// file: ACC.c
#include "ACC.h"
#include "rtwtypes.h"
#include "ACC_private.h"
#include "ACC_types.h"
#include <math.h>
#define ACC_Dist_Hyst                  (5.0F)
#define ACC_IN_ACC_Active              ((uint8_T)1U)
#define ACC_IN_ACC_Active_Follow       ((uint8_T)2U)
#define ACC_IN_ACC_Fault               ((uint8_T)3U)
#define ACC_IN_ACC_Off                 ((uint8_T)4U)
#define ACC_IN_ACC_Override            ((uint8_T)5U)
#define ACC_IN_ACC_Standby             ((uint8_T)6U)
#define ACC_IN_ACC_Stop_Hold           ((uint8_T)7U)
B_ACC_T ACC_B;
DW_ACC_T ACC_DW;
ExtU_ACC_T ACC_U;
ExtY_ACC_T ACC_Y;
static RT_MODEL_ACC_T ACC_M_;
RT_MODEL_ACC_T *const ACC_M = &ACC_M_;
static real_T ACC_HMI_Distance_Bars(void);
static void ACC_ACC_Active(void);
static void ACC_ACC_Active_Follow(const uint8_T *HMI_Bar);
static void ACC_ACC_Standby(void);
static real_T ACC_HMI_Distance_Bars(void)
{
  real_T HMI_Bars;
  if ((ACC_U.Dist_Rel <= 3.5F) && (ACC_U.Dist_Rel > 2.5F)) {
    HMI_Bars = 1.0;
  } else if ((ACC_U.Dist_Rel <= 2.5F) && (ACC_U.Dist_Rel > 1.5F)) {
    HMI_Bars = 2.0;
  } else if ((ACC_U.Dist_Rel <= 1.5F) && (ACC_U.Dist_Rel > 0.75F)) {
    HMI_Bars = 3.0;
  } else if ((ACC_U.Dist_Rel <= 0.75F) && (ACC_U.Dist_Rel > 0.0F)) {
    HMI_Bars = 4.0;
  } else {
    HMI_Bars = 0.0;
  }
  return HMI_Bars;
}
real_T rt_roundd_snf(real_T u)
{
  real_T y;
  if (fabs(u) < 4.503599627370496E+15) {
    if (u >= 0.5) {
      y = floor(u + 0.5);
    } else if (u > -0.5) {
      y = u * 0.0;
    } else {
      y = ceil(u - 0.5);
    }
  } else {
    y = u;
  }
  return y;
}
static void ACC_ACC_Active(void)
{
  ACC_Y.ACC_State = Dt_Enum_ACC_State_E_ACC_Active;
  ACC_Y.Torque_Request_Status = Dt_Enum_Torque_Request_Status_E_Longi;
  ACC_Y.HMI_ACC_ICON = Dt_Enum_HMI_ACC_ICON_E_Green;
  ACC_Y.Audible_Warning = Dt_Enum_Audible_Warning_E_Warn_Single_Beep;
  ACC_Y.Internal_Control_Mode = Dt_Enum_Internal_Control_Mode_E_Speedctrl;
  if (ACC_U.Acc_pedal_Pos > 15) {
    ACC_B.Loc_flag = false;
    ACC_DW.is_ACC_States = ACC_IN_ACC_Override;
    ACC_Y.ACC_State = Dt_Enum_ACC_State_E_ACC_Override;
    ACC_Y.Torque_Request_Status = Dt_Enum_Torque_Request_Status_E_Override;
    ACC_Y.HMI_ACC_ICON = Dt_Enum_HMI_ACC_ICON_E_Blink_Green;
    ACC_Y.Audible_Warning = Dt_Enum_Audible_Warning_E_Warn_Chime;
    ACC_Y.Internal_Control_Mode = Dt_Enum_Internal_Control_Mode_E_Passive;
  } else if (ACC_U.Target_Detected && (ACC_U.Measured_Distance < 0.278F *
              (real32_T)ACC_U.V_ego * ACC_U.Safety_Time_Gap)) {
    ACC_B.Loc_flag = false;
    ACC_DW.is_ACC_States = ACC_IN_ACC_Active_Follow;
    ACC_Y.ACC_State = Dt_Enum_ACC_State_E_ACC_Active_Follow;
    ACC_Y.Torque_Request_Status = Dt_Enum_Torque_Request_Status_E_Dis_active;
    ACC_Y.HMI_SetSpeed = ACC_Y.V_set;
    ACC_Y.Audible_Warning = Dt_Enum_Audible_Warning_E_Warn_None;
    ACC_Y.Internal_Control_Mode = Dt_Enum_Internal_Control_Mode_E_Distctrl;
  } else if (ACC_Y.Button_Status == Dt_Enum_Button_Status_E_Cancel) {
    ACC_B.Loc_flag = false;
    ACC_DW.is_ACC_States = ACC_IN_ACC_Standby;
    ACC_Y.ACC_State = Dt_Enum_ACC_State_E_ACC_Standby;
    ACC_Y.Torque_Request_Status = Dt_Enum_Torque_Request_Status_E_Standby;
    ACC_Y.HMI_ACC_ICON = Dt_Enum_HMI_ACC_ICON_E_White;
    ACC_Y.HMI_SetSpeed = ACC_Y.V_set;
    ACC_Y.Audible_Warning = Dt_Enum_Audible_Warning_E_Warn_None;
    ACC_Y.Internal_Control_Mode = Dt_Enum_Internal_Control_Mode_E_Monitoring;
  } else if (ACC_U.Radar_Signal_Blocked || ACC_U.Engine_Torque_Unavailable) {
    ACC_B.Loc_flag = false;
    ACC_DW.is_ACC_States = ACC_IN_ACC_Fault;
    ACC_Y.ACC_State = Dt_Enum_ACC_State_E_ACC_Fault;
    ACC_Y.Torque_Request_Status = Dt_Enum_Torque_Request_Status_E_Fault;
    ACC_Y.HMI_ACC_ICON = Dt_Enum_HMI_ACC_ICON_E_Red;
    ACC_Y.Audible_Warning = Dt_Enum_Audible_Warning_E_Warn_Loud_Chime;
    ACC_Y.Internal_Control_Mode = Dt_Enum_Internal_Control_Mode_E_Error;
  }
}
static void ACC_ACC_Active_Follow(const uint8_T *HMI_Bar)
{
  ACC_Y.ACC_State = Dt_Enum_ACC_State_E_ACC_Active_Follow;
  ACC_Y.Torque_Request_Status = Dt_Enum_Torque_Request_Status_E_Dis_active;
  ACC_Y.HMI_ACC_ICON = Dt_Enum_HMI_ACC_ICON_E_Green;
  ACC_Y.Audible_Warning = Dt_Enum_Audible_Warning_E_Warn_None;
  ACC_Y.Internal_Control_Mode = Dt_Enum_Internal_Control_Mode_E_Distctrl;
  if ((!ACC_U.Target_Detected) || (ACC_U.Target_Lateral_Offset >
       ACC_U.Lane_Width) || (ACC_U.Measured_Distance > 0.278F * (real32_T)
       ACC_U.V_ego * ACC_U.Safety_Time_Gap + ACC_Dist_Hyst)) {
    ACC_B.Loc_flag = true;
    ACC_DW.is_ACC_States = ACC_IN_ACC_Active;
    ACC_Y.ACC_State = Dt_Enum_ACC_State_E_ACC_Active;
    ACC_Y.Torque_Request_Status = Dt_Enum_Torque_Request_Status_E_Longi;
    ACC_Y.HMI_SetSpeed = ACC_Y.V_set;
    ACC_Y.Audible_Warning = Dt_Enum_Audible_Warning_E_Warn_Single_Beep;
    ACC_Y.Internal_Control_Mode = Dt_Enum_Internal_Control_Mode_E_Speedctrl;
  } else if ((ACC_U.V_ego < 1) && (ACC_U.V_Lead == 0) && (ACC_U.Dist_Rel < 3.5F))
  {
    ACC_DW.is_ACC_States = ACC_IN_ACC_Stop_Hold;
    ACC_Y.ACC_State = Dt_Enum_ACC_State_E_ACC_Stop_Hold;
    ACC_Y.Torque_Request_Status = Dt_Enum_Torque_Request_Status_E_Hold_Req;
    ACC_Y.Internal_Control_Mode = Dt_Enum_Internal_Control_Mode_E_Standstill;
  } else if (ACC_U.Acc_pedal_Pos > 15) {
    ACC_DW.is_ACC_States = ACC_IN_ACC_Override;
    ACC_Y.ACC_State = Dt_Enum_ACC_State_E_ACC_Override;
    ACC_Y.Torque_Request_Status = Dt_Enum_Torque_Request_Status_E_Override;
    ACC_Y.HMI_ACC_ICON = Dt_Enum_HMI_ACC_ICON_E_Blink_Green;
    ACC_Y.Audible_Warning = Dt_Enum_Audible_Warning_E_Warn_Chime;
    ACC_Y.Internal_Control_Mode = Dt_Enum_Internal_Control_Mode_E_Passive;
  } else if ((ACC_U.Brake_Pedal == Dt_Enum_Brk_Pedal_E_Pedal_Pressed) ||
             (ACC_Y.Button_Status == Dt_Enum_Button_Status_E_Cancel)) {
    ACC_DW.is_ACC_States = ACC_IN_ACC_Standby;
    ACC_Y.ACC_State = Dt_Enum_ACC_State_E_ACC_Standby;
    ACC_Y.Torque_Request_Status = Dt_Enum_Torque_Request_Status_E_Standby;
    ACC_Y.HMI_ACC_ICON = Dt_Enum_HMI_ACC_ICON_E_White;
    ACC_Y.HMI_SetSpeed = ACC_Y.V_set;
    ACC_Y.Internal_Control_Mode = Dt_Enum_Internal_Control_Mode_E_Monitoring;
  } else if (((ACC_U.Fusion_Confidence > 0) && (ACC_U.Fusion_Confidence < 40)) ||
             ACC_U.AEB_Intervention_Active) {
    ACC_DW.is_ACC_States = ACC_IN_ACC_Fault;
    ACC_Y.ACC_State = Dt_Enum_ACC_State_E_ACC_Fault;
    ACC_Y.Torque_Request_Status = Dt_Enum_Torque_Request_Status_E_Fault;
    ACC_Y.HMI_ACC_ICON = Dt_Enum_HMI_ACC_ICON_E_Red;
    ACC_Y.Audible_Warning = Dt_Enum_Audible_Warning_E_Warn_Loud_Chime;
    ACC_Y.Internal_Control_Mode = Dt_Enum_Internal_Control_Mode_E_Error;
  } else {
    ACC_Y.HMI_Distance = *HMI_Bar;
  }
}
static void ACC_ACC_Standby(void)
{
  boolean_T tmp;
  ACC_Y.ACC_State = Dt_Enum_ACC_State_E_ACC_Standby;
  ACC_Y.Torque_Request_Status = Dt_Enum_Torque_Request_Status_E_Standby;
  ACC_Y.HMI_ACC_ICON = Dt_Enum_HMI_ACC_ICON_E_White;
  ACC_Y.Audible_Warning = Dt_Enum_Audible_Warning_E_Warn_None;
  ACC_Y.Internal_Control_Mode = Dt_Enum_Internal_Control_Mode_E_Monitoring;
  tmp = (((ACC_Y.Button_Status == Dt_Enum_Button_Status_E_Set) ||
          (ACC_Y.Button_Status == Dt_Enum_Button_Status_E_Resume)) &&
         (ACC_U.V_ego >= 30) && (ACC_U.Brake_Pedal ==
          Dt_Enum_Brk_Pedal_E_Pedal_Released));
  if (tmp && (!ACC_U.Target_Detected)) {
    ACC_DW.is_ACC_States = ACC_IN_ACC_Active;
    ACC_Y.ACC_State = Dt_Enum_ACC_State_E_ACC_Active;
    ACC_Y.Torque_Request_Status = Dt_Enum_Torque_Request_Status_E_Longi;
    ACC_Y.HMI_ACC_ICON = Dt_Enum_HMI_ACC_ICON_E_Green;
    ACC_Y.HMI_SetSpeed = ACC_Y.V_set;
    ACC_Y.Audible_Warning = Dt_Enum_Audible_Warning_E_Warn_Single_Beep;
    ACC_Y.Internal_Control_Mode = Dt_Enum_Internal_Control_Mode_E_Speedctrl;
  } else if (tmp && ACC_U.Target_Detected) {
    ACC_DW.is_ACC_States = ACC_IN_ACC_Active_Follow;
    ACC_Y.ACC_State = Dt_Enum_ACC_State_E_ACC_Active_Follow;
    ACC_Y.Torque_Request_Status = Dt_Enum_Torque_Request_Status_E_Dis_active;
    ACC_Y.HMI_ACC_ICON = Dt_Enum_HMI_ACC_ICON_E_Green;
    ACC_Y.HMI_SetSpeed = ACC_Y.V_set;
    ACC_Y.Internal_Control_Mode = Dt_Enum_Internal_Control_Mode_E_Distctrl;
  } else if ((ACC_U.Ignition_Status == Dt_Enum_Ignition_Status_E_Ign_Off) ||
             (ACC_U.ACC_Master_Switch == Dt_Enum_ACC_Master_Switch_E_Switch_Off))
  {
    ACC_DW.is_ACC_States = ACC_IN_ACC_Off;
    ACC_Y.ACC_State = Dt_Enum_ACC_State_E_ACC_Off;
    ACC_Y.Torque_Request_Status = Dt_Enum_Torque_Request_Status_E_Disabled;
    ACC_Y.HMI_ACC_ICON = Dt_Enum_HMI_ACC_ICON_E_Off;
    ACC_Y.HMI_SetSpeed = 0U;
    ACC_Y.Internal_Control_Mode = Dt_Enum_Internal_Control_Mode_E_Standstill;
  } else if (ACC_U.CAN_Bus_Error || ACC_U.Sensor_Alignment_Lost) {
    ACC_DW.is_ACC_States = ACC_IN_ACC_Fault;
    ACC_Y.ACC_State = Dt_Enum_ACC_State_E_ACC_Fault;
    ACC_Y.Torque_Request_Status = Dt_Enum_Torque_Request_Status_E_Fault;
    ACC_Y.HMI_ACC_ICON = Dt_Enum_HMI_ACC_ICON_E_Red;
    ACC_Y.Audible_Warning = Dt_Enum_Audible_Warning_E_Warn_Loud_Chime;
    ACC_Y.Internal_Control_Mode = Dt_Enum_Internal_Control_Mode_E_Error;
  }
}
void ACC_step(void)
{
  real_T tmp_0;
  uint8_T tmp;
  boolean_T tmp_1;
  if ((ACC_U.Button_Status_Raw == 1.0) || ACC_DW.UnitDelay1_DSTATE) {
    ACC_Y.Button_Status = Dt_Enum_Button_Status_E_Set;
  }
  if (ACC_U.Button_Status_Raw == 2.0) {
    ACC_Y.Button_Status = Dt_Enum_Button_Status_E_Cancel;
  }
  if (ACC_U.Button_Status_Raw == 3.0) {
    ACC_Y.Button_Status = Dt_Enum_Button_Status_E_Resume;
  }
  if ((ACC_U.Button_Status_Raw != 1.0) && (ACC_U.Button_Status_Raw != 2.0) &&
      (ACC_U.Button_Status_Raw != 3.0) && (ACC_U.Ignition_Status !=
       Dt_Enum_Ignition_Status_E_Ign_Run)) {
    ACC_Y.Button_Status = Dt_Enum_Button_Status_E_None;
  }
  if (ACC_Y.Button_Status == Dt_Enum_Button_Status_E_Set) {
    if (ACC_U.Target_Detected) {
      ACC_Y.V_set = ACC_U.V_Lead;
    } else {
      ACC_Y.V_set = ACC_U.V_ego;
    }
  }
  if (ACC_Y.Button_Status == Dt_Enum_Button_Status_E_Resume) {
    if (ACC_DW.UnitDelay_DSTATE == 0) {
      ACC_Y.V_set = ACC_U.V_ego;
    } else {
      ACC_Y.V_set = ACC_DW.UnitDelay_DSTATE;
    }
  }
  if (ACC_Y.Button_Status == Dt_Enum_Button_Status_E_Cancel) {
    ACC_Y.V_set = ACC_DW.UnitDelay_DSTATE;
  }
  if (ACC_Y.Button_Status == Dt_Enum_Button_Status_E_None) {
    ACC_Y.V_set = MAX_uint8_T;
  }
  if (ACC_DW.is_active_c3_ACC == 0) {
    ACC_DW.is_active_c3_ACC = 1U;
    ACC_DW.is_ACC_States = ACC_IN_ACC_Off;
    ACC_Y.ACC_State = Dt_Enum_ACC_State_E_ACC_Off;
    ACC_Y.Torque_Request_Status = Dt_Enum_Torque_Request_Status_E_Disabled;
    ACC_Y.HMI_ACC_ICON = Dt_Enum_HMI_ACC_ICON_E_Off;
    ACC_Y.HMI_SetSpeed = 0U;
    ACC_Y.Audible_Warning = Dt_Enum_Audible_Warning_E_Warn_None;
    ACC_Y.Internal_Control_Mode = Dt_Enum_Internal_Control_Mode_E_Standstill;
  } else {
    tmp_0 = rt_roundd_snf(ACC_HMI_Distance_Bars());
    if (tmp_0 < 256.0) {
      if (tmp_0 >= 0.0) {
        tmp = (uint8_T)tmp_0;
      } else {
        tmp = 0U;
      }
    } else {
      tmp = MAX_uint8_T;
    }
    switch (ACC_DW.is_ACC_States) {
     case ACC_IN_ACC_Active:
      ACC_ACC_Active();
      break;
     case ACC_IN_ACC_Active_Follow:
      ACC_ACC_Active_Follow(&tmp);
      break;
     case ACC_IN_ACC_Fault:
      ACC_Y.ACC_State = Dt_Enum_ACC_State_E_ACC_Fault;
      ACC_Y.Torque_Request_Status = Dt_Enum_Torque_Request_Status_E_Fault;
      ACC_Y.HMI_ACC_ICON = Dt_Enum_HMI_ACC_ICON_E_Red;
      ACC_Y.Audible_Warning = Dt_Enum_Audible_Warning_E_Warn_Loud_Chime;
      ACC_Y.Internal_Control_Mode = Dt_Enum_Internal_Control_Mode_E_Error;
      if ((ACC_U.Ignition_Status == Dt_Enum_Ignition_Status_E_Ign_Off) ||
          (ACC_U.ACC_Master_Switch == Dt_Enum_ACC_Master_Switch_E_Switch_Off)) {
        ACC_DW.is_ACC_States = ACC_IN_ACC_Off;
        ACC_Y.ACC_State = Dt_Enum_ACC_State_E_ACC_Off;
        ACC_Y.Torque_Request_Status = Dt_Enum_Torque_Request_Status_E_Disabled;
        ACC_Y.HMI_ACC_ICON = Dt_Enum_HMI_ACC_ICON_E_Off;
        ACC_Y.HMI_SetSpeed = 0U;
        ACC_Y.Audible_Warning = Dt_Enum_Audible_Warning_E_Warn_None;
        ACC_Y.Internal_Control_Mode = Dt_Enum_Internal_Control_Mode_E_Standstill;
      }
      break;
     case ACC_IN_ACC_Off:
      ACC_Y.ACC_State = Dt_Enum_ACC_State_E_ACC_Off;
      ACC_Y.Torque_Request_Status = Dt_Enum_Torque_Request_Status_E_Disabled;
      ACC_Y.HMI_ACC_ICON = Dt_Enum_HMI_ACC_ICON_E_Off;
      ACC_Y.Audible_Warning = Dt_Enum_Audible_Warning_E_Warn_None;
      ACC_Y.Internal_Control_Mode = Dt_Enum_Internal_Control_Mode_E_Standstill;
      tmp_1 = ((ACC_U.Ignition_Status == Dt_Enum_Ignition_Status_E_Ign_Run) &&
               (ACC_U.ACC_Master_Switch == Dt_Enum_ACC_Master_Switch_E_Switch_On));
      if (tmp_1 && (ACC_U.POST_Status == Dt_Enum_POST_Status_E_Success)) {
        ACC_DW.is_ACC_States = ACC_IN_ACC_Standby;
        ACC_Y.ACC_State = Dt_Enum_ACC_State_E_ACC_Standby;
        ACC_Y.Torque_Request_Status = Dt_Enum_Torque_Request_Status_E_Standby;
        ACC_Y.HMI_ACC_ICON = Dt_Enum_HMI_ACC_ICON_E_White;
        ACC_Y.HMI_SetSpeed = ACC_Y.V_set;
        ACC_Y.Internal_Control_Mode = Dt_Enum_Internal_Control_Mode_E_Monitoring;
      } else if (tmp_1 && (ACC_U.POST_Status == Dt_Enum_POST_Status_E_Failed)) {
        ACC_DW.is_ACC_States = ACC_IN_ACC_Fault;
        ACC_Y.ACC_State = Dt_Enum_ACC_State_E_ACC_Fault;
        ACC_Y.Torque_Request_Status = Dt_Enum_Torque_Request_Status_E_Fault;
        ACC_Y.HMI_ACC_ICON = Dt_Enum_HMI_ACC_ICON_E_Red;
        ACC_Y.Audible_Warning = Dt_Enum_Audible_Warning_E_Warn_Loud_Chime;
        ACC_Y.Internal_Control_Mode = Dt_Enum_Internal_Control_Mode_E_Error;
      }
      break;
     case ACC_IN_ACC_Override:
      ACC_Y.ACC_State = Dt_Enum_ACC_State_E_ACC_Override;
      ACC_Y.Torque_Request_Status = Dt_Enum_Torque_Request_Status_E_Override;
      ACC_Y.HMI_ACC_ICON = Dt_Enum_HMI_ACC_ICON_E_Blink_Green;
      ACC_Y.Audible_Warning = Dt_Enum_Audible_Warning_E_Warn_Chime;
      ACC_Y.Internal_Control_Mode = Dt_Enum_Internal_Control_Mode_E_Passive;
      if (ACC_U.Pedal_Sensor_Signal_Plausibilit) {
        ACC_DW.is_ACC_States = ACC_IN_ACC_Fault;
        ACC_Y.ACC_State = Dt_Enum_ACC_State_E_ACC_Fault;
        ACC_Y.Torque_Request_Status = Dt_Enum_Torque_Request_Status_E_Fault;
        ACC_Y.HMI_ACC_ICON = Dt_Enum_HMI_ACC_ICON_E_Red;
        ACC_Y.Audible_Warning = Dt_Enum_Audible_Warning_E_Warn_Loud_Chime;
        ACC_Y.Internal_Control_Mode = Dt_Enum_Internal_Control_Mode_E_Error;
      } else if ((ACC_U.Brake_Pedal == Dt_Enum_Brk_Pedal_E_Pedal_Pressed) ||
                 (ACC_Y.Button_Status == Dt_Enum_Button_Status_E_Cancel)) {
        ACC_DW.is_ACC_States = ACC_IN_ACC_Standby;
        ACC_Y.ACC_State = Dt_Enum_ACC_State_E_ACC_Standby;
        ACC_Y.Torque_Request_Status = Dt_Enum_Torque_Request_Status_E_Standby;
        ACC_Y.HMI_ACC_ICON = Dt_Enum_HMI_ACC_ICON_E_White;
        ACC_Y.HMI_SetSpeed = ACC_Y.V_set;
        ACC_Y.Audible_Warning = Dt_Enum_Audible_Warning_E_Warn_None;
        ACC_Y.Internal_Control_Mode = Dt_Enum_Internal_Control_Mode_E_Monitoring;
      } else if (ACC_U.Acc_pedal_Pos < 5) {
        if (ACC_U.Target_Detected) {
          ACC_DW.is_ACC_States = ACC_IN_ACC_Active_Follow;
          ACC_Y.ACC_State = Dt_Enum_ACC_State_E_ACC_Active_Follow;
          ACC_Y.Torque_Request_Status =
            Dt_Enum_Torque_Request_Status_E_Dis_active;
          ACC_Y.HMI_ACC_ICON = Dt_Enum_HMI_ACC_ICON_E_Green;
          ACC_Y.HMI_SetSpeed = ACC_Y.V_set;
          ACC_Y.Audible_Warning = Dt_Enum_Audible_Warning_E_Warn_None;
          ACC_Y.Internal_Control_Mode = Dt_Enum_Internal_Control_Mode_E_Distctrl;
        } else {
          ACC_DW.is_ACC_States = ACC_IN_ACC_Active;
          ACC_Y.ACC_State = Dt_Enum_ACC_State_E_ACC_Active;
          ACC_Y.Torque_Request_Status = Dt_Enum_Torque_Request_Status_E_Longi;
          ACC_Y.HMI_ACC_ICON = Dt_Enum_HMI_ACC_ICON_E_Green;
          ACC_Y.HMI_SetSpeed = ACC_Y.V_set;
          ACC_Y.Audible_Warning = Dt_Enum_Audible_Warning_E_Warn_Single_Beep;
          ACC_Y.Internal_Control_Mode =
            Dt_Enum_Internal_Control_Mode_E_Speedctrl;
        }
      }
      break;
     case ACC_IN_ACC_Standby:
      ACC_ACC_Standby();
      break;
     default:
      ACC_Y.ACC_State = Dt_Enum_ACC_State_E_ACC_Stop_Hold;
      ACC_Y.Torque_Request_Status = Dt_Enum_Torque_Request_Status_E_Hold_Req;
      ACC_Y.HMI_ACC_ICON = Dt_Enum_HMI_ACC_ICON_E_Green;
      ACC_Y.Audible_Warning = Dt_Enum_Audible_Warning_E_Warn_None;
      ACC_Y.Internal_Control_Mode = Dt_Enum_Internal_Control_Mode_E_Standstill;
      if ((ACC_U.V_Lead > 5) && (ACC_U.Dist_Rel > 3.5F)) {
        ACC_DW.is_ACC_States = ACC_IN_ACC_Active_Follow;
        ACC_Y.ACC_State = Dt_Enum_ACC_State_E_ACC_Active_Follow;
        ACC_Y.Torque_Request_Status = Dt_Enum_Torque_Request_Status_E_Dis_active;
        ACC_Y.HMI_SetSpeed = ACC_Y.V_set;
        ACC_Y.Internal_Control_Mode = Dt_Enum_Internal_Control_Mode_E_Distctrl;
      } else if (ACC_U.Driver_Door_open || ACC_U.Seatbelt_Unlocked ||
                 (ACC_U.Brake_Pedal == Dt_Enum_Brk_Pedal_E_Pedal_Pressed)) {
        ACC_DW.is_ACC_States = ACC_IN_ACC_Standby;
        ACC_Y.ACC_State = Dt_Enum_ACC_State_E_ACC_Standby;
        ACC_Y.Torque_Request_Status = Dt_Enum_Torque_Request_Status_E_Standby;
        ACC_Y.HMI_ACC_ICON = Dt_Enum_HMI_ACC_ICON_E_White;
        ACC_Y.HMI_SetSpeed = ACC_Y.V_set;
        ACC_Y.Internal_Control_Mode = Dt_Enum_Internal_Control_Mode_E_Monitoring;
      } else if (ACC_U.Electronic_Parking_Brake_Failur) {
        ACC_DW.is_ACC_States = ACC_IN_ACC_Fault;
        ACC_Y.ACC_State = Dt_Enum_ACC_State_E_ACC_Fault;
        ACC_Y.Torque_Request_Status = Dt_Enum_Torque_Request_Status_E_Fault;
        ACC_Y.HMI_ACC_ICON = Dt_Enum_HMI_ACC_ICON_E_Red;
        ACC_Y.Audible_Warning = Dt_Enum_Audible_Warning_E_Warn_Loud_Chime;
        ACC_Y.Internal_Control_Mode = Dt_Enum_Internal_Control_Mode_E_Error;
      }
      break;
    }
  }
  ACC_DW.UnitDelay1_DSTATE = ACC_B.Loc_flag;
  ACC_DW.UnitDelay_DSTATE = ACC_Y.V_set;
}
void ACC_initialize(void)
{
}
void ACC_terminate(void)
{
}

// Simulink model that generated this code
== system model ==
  Button_Status_Raw : Inport
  ACC_Master_Switch : Inport
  AEB_Intervention_Active : Inport
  Acc_pedal_Pos : Inport
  Brake_Pedal : Inport
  CAN_Bus_Error : Inport
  Dist_Rel : Inport
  Driver_Door_open : Inport
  Inport#1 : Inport
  Engine_Torque_Unavailable : Inport
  Fusion_Confidence : Inport
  Ignition_Status : Inport
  Lane_Width : Inport
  Measured_Distance : Inport
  POST_Status : Inport
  Inport#2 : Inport
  Radar_Signal_Blocked : Inport
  Target_Detected : Inport
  Seatbelt_Unlocked : Inport
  Sensor_Alignment_Lost : Inport
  Target_Lateral_Offset : Inport
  V_Lead : Inport
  V_ego : Inport
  Safety_Time_Gap : Inport
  Audible_Warning : Outport  <- 1: ACC
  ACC : Stateflow chart  <- 1: ACC_Master_Switch, 2: AEB_Intervention_Active, 3: Acc_pedal_Pos, 4: Brake_Pedal, 5: CAN_Bus_Error, 6: Dist_Rel, 7: Driver_Door_open, 8: Inport#1, 9: Engine_Torque_Unavailable, 10: Fusion_Confidence, 11: Ignition_Status, 12: Lane_Width, 13: Measured_Distance, 14: POST_Status, 15: Inport#2, 16: Radar_Signal_Blocked, 17: Target_Detected, 18: Seatbelt_Unlocked, 19: Sensor_Alignment_Lost, 20: Target_Lateral_Offset, 21: V_Lead, 22: V_ego, 23: Stateflowchart#1, 24: Safety_Time_Gap, 25: Stateflowchart#2
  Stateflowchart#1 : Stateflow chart  <- 1: Button_Status_Raw, 2: Ignition_Status, 3: UnitDelay1
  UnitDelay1 : UnitDelay  <- 1: ACC/8
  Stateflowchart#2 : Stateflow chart  <- 1: Stateflowchart#1, 2: V_ego, 3: UnitDelay, 4: V_Lead, 5: Target_Detected
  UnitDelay : UnitDelay  <- 1: Stateflowchart#2
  HMI_ACC_ICON : Outport  <- 1: ACC/2
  HMI_SetSpeed : Outport  <- 1: ACC/3
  Torque_Request_Status : Outport  <- 1: ACC/4
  Internal_Control_Mode : Outport  <- 1: ACC/5
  HMI_Distance : Outport  <- 1: ACC/6
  ACC_State : Outport  <- 1: ACC/7
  Button_Status : Outport  <- 1: Stateflowchart#1
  V_set : Outport  <- 1: Stateflowchart#2
== stateflow chart Stateflowchart#1 ==
  (default) -> (junction 29)
  (junction 29) -> (junction 4) [order 1] : [Button_Status_Raw == 1 || Loc_flag]
  (junction 29) -> (junction 8) [order 2]
  (junction 4) -> (junction 6) : {Button_Status = Set}
  (junction 6) -> (junction 8)
  (junction 8) -> (junction 11)
  (junction 11) -> (junction 13) [order 1] : [Button_Status_Raw == 2]
  (junction 11) -> (junction 17) [order 2]
  (junction 13) -> (junction 15) : {Button_Status = Cancel}
  (junction 15) -> (junction 17)
  (junction 17) -> (junction 20)
  (junction 20) -> (junction 32) [order 1] : [Button_Status_Raw == 3]
  (junction 20) -> (junction 35) [order 2]
  (junction 32) -> (junction 34) : {Button_Status = Resume}
  (junction 34) -> (junction 35)
  (junction 35) -> (junction 40)
  (junction 40) -> (junction 39) [order 1] : [(Button_Status_Raw ~= 1 && Button_Status_Raw ~=2 && Button_Status_Raw ~= 3) && (Ignition_Status ~= Ign_Run)]
  (junction 40) -> (junction 42) [order 2]
  (junction 39) -> (junction 41) : {Button_Status = None}
  (junction 41) -> (junction 42)
  data: Button_Status_Raw input; Button_Status output Enum: Dt_Enum_Button_Status_E; Ignition_Status input Enum: Dt_Enum_Ignition_Status_E; Loc_flag input

== stateflow chart Stateflowchart#2 ==
  (default) -> (junction 2)
  (junction 2) -> (junction 3) [order 1] : [ Button_Status ==Set]
  (junction 3) -> (junction 42) [order 1] : [Target_Detected]
  (junction 2) -> (junction 4) [order 2]
  (junction 3) -> (junction 1) [order 2] : {V_set = V_ego}
  (junction 42) -> (junction 44) : {V_set = V_Lead}
  (junction 1) -> (junction 4)
  (junction 44) -> (junction 1)
  (junction 4) -> (junction 9)
  (junction 9) -> (junction 7) [order 1] : [Button_Status == Resume]
  (junction 7) -> (junction 34) [order 2]
  (junction 34) -> (junction 10) : {V_set = V_set_Prev}
  (junction 9) -> (junction 5) [order 2]
  (junction 7) -> (junction 39) [order 1] : [V_set_Prev ==0 ]
  (junction 39) -> (junction 10) : {V_set = V_ego}
  (junction 10) -> (junction 5)
  (junction 5) -> (junction 53)
  (junction 53) -> (junction 55) [order 1] : [Button_Status == Cancel]
  (junction 53) -> (junction 59) [order 2]
  (junction 55) -> (junction 57) : {V_set = V_set_Prev}
  (junction 57) -> (junction 59)
  (junction 59) -> (junction 62)
  (junction 62) -> (junction 64) [order 1] : [Button_Status == None]
  (junction 62) -> (junction 68) [order 2]
  (junction 64) -> (junction 66) : {V_set = 255}
  (junction 66) -> (junction 68)
  data: Button_Status input Enum: Dt_Enum_Button_Status_E; V_ego input uint8; V_set output uint8; V_set_Prev input uint8; V_Lead input; Target_Detected input

== stateflow chart ACC ==
  state HMI_Bars = HMI_Distance_Bars [function]
    (junction 523) -> (junction 533) : {HMI_Bars=1}
    (junction 521) -> (junction 523) [order 1] : [Dist_Rel <= 3.5 && Dist_Rel > 2.5]
    (junction 524) -> (junction 533) : {HMI_Bars=2}
    (junction 521) -> (junction 524) [order 2] : [Dist_Rel <= 2.5 && Dist_Rel > 1.5]
    (default) -> (junction 521)
    (junction 525) -> (junction 533) : {HMI_Bars=3}
    (junction 521) -> (junction 525) [order 3] : [Dist_Rel <= 1.5 && Dist_Rel > 0.75]
    (junction 521) -> (junction 526) [order 4] : [Dist_Rel <= 0.75 && Dist_Rel > 0]
    (junction 521) -> (junction 527) [order 5]
    (junction 526) -> (junction 533) : {HMI_Bars=4}
    (junction 527) -> (junction 533) : {HMI_Bars=0}
  state ACC_States [parallel]
    du:
    HMI_Bar = uint8(HMI_Distance_Bars())
    settings: executionOrder=1
    state ACC_Fault
      en:
      ACC_Status = 2;
      ACC_State = ACC_Fault;
      Torque_Request_Status = Fault;
      HMI_ACC_ICON = Red;
      Audible_Warning = Warn_Loud_Chime;
      Internal_Control_Mode = Error;
    state ACC_Off
      en:
      ACC_Status = 0;
      ACC_State = ACC_Off;
      Torque_Request_Status = Disabled;
      HMI_ACC_ICON = Off;
      HMI_SetSpeed = 0;
      Audible_Warning = Warn_None;
      Internal_Control_Mode = Standstill;
    state ACC_Override
      en:
      ACC_Status = 6;
      ACC_State = ACC_Override;
      Torque_Request_Status = Override;
      HMI_ACC_ICON = Blink_Green;
      Audible_Warning = Warn_Chime;%V>Vset for x
      Internal_Control_Mode = Passive;
    state ACC_Active
      en:
      ACC_Status = 3;
      ACC_State = ACC_Active;
      Torque_Request_Status = Longi;
      HMI_ACC_ICON = Green;
      HMI_SetSpeed = V_set;%Current_SetSpeed
      Audible_Warning = Warn_Single_Beep;
      Internal_Control_Mode = Speedctrl;
      ex:
      Loc_flag=false;
    state ACC_Active_Follow
      en:
      ACC_Status = 4;
      ACC_State =  ACC_Active_Follow;
      %Drel Cal
      Torque_Request_Status = Dis_active;
      HMI_ACC_ICON = Green;
      HMI_SetSpeed = V_set;%New_SetSpeed_Target
      Audible_Warning = Warn_None;
      Internal_Control_Mode = Distctrl;
      du:
      HMI_Distance = HMI_Bar;%1-5 Bars
    state ACC_Standby
      en:
      ACC_Status = 1;
      ACC_State = ACC_Standby;
      Torque_Request_Status = Standby;
      HMI_ACC_ICON = White;
      HMI_SetSpeed = V_set;%Prev Speed
      Audible_Warning = Warn_None;
      Internal_Control_Mode = Monitoring;
    state ACC_Stop_Hold
      en:
      ACC_Status = 5;
      ACC_State = ACC_Stop_Hold;
      Torque_Request_Status = Hold_Req;
      HMI_ACC_ICON = Green;
      Audible_Warning = Warn_None;
      Internal_Control_Mode = Standstill;
    (junction 371) -> (junction 378)
    (junction 384) -> (junction 371)
    (junction 378) -> (junction 373)
    (junction 383) -> (junction 373)
    (junction 374) -> (junction 373)
    (junction 386) -> (junction 383)
    (junction 373) -> ACC_Fault
    (junction 380) -> (junction 374)
    (default) -> ACC_Off
    ACC_Override -> (junction 375) [order 2] : [Brake_Pedal == Pedal_Pressed || ...
        | Button_Status == Cancel]
    (junction 375) -> (junction 425)
    ACC_Off -> ACC_Fault [order 2] : [Ignition_Status == Ign_Run &&...
        | ACC_Master_Switch == Switch_On &&...
        | POST_Status == Failed]
    ACC_Active_Follow -> ACC_Override [order 3] : [Acc_pedal_Pos > 15]
    ACC_Override -> ACC_Fault [order 1] : [Pedal_Sensor_Signal_Plausibility_Error == true  ]
    ACC_Fault -> ACC_Off : [Ignition_Status == Ign_Off ||...
        | ACC_Master_Switch == Switch_Off]
    ACC_Active -> ACC_Fault [order 4] : [Radar_Signal_Blocked == true || ...
        | Engine_Torque_Unavailable == true]
    ACC_Active -> ACC_Override [order 1] : [Acc_pedal_Pos > 15]
    ACC_Override -> (junction 556) [order 3] : [Acc_pedal_Pos < 5 ]
    ACC_Off -> ACC_Standby [order 1] : [Ignition_Status == Ign_Run &&...
        | ACC_Master_Switch == Switch_On &&...
        | POST_Status == Success]
    ACC_Standby -> ACC_Off [order 3] : [Ignition_Status == Ign_Off ||...
        | ACC_Master_Switch == Switch_Off]
    (junction 556) -> ACC_Active_Follow [order 1] : [ Target_Detected == true]
    (junction 556) -> ACC_Active [order 2] : [ Target_Detected == false]
    ACC_Active_Follow -> (junction 380) [order 5] : [ ( Fusion_Confidence > 0 && Fusion_Confidence < 40) || AEB_Intervention_Active == true]
    ACC_Standby -> (junction 386) [order 4] : [CAN_Bus_Error == true ||...
        | Sensor_Alignment_Lost == true]
    ACC_Active -> ACC_Standby [order 3] : [Button_Status == Cancel]
    ACC_Active -> ACC_Active_Follow [order 2] : [Target_Detected == true &&...
        |  Measured_Distance < (single(0.278*single(V_ego)*Safety_Time_Gap))]
    (junction 381) -> ACC_Standby
    (junction 408) -> (junction 381)
    ACC_Standby -> ACC_Active [order 1] : [(Button_Status == Set || ...
        | Button_Status == Resume) && ...
        | V_ego >= 30 && ...
        | Brake_Pedal == Pedal_Released && ...
        | Target_Detected == false]
    ACC_Active_Follow -> ACC_Active [order 1] : [Target_Detected == false ||...
        | Target_Lateral_Offset > Lane_Width ||...
        |  Measured_Distance > (single(0.278*single(V_ego)*Safety_Time_Gap)+Dist_Hyst)]/{Loc_flag=true;}
    (junction 382) -> ACC_Standby
    (junction 421) -> (junction 382)
    ACC_Standby -> ACC_Active_Follow [order 2] : [(Button_Status == Set ||...
        | Button_Status == Resume) && ...
        | V_ego >= 30 && ...
        | Brake_Pedal == Pedal_Released && ...
        | Target_Detected == true]
    ACC_Stop_Hold -> ACC_Standby [order 2] : [Driver_Door_open == true || ...
        | Seatbelt_Unlocked == true || ...
        | Brake_Pedal == Pedal_Pressed]
    ACC_Stop_Hold -> ACC_Active_Follow [order 1] : [ V_Lead > 5 && Dist_Rel > 3.5]
    ACC_Active_Follow -> ACC_Stop_Hold [order 2] : [V_ego < 1 && V_Lead == 0 && Dist_Rel < 3.5]
    ACC_Active_Follow -> (junction 397) [order 4] : [Brake_Pedal == Pedal_Pressed || Button_Status == Cancel]
    ACC_Stop_Hold -> (junction 384) [order 3] : [Electronic_Parking_Brake_Failure == true]
    (junction 397) -> (junction 421)
    (junction 425) -> (junction 408)
  data: HMI_Bars function_output; ACC_Master_Switch input Enum: Dt_Enum_ACC_Master_Switch_E; AEB_Intervention_Active input boolean; Acc_pedal_Pos input uint8; Brake_Pedal input Enum: Dt_Enum_Brk_Pedal_E; CAN_Bus_Error input boolean; Dist_Rel input single; Driver_Door_open input boolean; Electronic_Parking_Brake_Failure input boolean; Engine_Torque_Unavailable input boolean; Fusion_Confidence input uint8; Ignition_Status input Enum: Dt_Enum_Ignition_Status_E; Lane_Width input uint16; Measured_Distance input single; POST_Status input Enum: Dt_Enum_POST_Status_E; Pedal_Sensor_Signal_Plausibility_Error input boolean; Radar_Signal_Blocked input boolean; Target_Detected input boolean; Seatbelt_Unlocked input boolean; Sensor_Alignment_Lost input boolean; Target_Lateral_Offset input uint16; V_Lead input uint8; V_ego input uint8; Button_Status input Enum: Dt_Enum_Button_Status_E; Safety_Time_Gap input single; Audible_Warning output Enum: Dt_Enum_Audible_Warning_E; HMI_ACC_ICON output Enum: Dt_Enum_HMI_ACC_ICON_E; HMI_SetSpeed output uint8; Torque_Request_Status output Enum: Dt_Enum_Torque_Request_Status_E; Internal_Control_Mode output Enum: Dt_Enum_Internal_Control_Mode_E; HMI_Distance output uint8; ACC_Status local uint8 =0; V_set input uint8; ACC_State output Enum: Dt_Enum_ACC_State_E; HMI_Bar local uint8; Dist_Hyst constant single =5; Loc_flag output boolean
